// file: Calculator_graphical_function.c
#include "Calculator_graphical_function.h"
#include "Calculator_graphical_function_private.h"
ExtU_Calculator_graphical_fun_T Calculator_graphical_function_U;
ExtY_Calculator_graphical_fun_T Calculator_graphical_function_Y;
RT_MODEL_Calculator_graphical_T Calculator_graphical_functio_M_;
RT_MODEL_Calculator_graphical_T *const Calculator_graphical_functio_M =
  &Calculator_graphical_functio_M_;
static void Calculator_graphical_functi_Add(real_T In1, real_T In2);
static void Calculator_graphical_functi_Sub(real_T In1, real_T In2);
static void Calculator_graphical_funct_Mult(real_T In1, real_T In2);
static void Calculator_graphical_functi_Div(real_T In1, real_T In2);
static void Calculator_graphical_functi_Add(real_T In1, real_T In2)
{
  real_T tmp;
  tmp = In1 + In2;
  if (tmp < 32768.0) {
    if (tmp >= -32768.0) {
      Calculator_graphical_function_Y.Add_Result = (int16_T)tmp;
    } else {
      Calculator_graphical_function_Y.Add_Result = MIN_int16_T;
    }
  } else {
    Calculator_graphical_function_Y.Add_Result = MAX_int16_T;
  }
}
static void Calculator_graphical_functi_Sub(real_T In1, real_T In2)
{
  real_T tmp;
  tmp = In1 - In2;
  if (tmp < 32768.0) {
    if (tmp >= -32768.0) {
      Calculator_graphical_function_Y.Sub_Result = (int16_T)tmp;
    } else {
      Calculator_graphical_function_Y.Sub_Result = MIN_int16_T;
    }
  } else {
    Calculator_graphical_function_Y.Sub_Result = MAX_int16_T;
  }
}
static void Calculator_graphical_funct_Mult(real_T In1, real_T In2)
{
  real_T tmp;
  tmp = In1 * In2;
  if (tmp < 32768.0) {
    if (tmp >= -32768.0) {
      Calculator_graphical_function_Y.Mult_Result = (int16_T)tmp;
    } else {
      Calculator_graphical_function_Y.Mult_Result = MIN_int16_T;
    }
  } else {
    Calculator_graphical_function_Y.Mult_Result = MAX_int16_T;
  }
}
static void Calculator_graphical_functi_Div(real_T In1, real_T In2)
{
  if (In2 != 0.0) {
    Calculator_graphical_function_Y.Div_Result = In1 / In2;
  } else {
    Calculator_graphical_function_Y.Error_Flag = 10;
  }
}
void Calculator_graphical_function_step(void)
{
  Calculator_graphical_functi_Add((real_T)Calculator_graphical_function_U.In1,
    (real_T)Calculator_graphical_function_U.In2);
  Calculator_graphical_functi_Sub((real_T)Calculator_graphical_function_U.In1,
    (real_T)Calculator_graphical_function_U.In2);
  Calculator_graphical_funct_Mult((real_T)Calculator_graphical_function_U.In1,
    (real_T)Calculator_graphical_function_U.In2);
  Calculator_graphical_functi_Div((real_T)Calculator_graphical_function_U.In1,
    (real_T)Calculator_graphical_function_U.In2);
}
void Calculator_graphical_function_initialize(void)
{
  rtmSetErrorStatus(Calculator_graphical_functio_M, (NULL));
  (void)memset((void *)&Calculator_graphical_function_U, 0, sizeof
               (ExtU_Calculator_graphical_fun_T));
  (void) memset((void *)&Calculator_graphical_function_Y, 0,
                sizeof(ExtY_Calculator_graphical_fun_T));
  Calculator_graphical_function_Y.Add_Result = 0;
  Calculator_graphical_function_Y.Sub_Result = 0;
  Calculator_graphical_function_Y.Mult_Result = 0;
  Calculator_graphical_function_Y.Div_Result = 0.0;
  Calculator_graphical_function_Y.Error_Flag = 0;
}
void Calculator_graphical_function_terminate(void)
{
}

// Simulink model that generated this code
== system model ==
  In1 : Inport
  In2 : Inport
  Add_Result : Outport  <- 1: Stateflowchart#1
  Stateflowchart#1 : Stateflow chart  <- 1: In1, 2: In2
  Sub_Result : Outport  <- 1: Stateflowchart#1/2
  Mult_Result : Outport  <- 1: Stateflowchart#1/3
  Div_Result : Outport  <- 1: Stateflowchart#1/4
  Error_Flag : Outport  <- 1: Stateflowchart#1/5
== stateflow chart Stateflowchart#1 ==
  state Add(In1,In2) [function]
    (default) -> (junction 11) : {Result_Add = In1+In2;}
  state Sub(In1,In2) [function]
    (default) -> (junction 20) : {Result_Subs = In1-In2;}
  state Mult(In1,In2) [function]
    (default) -> (junction 25) : {Result_Mult = In1*In2;}
  state Div(In1,In2) [function]
    (default) -> (junction 46) : /* Division */
    (junction 46) -> (junction 47) [order 1] : [In2!=0]
    (junction 46) -> (junction 48) [order 2] : {Error_Flag=10;}
    (junction 47) -> (junction 49) : {Result_Div = In1/In2;}
    (junction 49) -> (junction 48)
    (junction 48) -> (junction 50)
  (default) -> (junction 4) : {Add(In1,In2);
      | Sub(In1,In2);
      | Mult(In1,In2);
      | Div(In1,In2);
      | }
  data: In1 function_input double; In2 function_input double; In1 function_input double; In2 function_input double; In1 function_input double; In2 function_input double; In1 function_input double; In2 function_input double; In1 input int16; In2 input int16; Result_Add output int16; Result_Subs output int16; Result_Mult output int16; Result_Div output double; Error_Flag output int16
